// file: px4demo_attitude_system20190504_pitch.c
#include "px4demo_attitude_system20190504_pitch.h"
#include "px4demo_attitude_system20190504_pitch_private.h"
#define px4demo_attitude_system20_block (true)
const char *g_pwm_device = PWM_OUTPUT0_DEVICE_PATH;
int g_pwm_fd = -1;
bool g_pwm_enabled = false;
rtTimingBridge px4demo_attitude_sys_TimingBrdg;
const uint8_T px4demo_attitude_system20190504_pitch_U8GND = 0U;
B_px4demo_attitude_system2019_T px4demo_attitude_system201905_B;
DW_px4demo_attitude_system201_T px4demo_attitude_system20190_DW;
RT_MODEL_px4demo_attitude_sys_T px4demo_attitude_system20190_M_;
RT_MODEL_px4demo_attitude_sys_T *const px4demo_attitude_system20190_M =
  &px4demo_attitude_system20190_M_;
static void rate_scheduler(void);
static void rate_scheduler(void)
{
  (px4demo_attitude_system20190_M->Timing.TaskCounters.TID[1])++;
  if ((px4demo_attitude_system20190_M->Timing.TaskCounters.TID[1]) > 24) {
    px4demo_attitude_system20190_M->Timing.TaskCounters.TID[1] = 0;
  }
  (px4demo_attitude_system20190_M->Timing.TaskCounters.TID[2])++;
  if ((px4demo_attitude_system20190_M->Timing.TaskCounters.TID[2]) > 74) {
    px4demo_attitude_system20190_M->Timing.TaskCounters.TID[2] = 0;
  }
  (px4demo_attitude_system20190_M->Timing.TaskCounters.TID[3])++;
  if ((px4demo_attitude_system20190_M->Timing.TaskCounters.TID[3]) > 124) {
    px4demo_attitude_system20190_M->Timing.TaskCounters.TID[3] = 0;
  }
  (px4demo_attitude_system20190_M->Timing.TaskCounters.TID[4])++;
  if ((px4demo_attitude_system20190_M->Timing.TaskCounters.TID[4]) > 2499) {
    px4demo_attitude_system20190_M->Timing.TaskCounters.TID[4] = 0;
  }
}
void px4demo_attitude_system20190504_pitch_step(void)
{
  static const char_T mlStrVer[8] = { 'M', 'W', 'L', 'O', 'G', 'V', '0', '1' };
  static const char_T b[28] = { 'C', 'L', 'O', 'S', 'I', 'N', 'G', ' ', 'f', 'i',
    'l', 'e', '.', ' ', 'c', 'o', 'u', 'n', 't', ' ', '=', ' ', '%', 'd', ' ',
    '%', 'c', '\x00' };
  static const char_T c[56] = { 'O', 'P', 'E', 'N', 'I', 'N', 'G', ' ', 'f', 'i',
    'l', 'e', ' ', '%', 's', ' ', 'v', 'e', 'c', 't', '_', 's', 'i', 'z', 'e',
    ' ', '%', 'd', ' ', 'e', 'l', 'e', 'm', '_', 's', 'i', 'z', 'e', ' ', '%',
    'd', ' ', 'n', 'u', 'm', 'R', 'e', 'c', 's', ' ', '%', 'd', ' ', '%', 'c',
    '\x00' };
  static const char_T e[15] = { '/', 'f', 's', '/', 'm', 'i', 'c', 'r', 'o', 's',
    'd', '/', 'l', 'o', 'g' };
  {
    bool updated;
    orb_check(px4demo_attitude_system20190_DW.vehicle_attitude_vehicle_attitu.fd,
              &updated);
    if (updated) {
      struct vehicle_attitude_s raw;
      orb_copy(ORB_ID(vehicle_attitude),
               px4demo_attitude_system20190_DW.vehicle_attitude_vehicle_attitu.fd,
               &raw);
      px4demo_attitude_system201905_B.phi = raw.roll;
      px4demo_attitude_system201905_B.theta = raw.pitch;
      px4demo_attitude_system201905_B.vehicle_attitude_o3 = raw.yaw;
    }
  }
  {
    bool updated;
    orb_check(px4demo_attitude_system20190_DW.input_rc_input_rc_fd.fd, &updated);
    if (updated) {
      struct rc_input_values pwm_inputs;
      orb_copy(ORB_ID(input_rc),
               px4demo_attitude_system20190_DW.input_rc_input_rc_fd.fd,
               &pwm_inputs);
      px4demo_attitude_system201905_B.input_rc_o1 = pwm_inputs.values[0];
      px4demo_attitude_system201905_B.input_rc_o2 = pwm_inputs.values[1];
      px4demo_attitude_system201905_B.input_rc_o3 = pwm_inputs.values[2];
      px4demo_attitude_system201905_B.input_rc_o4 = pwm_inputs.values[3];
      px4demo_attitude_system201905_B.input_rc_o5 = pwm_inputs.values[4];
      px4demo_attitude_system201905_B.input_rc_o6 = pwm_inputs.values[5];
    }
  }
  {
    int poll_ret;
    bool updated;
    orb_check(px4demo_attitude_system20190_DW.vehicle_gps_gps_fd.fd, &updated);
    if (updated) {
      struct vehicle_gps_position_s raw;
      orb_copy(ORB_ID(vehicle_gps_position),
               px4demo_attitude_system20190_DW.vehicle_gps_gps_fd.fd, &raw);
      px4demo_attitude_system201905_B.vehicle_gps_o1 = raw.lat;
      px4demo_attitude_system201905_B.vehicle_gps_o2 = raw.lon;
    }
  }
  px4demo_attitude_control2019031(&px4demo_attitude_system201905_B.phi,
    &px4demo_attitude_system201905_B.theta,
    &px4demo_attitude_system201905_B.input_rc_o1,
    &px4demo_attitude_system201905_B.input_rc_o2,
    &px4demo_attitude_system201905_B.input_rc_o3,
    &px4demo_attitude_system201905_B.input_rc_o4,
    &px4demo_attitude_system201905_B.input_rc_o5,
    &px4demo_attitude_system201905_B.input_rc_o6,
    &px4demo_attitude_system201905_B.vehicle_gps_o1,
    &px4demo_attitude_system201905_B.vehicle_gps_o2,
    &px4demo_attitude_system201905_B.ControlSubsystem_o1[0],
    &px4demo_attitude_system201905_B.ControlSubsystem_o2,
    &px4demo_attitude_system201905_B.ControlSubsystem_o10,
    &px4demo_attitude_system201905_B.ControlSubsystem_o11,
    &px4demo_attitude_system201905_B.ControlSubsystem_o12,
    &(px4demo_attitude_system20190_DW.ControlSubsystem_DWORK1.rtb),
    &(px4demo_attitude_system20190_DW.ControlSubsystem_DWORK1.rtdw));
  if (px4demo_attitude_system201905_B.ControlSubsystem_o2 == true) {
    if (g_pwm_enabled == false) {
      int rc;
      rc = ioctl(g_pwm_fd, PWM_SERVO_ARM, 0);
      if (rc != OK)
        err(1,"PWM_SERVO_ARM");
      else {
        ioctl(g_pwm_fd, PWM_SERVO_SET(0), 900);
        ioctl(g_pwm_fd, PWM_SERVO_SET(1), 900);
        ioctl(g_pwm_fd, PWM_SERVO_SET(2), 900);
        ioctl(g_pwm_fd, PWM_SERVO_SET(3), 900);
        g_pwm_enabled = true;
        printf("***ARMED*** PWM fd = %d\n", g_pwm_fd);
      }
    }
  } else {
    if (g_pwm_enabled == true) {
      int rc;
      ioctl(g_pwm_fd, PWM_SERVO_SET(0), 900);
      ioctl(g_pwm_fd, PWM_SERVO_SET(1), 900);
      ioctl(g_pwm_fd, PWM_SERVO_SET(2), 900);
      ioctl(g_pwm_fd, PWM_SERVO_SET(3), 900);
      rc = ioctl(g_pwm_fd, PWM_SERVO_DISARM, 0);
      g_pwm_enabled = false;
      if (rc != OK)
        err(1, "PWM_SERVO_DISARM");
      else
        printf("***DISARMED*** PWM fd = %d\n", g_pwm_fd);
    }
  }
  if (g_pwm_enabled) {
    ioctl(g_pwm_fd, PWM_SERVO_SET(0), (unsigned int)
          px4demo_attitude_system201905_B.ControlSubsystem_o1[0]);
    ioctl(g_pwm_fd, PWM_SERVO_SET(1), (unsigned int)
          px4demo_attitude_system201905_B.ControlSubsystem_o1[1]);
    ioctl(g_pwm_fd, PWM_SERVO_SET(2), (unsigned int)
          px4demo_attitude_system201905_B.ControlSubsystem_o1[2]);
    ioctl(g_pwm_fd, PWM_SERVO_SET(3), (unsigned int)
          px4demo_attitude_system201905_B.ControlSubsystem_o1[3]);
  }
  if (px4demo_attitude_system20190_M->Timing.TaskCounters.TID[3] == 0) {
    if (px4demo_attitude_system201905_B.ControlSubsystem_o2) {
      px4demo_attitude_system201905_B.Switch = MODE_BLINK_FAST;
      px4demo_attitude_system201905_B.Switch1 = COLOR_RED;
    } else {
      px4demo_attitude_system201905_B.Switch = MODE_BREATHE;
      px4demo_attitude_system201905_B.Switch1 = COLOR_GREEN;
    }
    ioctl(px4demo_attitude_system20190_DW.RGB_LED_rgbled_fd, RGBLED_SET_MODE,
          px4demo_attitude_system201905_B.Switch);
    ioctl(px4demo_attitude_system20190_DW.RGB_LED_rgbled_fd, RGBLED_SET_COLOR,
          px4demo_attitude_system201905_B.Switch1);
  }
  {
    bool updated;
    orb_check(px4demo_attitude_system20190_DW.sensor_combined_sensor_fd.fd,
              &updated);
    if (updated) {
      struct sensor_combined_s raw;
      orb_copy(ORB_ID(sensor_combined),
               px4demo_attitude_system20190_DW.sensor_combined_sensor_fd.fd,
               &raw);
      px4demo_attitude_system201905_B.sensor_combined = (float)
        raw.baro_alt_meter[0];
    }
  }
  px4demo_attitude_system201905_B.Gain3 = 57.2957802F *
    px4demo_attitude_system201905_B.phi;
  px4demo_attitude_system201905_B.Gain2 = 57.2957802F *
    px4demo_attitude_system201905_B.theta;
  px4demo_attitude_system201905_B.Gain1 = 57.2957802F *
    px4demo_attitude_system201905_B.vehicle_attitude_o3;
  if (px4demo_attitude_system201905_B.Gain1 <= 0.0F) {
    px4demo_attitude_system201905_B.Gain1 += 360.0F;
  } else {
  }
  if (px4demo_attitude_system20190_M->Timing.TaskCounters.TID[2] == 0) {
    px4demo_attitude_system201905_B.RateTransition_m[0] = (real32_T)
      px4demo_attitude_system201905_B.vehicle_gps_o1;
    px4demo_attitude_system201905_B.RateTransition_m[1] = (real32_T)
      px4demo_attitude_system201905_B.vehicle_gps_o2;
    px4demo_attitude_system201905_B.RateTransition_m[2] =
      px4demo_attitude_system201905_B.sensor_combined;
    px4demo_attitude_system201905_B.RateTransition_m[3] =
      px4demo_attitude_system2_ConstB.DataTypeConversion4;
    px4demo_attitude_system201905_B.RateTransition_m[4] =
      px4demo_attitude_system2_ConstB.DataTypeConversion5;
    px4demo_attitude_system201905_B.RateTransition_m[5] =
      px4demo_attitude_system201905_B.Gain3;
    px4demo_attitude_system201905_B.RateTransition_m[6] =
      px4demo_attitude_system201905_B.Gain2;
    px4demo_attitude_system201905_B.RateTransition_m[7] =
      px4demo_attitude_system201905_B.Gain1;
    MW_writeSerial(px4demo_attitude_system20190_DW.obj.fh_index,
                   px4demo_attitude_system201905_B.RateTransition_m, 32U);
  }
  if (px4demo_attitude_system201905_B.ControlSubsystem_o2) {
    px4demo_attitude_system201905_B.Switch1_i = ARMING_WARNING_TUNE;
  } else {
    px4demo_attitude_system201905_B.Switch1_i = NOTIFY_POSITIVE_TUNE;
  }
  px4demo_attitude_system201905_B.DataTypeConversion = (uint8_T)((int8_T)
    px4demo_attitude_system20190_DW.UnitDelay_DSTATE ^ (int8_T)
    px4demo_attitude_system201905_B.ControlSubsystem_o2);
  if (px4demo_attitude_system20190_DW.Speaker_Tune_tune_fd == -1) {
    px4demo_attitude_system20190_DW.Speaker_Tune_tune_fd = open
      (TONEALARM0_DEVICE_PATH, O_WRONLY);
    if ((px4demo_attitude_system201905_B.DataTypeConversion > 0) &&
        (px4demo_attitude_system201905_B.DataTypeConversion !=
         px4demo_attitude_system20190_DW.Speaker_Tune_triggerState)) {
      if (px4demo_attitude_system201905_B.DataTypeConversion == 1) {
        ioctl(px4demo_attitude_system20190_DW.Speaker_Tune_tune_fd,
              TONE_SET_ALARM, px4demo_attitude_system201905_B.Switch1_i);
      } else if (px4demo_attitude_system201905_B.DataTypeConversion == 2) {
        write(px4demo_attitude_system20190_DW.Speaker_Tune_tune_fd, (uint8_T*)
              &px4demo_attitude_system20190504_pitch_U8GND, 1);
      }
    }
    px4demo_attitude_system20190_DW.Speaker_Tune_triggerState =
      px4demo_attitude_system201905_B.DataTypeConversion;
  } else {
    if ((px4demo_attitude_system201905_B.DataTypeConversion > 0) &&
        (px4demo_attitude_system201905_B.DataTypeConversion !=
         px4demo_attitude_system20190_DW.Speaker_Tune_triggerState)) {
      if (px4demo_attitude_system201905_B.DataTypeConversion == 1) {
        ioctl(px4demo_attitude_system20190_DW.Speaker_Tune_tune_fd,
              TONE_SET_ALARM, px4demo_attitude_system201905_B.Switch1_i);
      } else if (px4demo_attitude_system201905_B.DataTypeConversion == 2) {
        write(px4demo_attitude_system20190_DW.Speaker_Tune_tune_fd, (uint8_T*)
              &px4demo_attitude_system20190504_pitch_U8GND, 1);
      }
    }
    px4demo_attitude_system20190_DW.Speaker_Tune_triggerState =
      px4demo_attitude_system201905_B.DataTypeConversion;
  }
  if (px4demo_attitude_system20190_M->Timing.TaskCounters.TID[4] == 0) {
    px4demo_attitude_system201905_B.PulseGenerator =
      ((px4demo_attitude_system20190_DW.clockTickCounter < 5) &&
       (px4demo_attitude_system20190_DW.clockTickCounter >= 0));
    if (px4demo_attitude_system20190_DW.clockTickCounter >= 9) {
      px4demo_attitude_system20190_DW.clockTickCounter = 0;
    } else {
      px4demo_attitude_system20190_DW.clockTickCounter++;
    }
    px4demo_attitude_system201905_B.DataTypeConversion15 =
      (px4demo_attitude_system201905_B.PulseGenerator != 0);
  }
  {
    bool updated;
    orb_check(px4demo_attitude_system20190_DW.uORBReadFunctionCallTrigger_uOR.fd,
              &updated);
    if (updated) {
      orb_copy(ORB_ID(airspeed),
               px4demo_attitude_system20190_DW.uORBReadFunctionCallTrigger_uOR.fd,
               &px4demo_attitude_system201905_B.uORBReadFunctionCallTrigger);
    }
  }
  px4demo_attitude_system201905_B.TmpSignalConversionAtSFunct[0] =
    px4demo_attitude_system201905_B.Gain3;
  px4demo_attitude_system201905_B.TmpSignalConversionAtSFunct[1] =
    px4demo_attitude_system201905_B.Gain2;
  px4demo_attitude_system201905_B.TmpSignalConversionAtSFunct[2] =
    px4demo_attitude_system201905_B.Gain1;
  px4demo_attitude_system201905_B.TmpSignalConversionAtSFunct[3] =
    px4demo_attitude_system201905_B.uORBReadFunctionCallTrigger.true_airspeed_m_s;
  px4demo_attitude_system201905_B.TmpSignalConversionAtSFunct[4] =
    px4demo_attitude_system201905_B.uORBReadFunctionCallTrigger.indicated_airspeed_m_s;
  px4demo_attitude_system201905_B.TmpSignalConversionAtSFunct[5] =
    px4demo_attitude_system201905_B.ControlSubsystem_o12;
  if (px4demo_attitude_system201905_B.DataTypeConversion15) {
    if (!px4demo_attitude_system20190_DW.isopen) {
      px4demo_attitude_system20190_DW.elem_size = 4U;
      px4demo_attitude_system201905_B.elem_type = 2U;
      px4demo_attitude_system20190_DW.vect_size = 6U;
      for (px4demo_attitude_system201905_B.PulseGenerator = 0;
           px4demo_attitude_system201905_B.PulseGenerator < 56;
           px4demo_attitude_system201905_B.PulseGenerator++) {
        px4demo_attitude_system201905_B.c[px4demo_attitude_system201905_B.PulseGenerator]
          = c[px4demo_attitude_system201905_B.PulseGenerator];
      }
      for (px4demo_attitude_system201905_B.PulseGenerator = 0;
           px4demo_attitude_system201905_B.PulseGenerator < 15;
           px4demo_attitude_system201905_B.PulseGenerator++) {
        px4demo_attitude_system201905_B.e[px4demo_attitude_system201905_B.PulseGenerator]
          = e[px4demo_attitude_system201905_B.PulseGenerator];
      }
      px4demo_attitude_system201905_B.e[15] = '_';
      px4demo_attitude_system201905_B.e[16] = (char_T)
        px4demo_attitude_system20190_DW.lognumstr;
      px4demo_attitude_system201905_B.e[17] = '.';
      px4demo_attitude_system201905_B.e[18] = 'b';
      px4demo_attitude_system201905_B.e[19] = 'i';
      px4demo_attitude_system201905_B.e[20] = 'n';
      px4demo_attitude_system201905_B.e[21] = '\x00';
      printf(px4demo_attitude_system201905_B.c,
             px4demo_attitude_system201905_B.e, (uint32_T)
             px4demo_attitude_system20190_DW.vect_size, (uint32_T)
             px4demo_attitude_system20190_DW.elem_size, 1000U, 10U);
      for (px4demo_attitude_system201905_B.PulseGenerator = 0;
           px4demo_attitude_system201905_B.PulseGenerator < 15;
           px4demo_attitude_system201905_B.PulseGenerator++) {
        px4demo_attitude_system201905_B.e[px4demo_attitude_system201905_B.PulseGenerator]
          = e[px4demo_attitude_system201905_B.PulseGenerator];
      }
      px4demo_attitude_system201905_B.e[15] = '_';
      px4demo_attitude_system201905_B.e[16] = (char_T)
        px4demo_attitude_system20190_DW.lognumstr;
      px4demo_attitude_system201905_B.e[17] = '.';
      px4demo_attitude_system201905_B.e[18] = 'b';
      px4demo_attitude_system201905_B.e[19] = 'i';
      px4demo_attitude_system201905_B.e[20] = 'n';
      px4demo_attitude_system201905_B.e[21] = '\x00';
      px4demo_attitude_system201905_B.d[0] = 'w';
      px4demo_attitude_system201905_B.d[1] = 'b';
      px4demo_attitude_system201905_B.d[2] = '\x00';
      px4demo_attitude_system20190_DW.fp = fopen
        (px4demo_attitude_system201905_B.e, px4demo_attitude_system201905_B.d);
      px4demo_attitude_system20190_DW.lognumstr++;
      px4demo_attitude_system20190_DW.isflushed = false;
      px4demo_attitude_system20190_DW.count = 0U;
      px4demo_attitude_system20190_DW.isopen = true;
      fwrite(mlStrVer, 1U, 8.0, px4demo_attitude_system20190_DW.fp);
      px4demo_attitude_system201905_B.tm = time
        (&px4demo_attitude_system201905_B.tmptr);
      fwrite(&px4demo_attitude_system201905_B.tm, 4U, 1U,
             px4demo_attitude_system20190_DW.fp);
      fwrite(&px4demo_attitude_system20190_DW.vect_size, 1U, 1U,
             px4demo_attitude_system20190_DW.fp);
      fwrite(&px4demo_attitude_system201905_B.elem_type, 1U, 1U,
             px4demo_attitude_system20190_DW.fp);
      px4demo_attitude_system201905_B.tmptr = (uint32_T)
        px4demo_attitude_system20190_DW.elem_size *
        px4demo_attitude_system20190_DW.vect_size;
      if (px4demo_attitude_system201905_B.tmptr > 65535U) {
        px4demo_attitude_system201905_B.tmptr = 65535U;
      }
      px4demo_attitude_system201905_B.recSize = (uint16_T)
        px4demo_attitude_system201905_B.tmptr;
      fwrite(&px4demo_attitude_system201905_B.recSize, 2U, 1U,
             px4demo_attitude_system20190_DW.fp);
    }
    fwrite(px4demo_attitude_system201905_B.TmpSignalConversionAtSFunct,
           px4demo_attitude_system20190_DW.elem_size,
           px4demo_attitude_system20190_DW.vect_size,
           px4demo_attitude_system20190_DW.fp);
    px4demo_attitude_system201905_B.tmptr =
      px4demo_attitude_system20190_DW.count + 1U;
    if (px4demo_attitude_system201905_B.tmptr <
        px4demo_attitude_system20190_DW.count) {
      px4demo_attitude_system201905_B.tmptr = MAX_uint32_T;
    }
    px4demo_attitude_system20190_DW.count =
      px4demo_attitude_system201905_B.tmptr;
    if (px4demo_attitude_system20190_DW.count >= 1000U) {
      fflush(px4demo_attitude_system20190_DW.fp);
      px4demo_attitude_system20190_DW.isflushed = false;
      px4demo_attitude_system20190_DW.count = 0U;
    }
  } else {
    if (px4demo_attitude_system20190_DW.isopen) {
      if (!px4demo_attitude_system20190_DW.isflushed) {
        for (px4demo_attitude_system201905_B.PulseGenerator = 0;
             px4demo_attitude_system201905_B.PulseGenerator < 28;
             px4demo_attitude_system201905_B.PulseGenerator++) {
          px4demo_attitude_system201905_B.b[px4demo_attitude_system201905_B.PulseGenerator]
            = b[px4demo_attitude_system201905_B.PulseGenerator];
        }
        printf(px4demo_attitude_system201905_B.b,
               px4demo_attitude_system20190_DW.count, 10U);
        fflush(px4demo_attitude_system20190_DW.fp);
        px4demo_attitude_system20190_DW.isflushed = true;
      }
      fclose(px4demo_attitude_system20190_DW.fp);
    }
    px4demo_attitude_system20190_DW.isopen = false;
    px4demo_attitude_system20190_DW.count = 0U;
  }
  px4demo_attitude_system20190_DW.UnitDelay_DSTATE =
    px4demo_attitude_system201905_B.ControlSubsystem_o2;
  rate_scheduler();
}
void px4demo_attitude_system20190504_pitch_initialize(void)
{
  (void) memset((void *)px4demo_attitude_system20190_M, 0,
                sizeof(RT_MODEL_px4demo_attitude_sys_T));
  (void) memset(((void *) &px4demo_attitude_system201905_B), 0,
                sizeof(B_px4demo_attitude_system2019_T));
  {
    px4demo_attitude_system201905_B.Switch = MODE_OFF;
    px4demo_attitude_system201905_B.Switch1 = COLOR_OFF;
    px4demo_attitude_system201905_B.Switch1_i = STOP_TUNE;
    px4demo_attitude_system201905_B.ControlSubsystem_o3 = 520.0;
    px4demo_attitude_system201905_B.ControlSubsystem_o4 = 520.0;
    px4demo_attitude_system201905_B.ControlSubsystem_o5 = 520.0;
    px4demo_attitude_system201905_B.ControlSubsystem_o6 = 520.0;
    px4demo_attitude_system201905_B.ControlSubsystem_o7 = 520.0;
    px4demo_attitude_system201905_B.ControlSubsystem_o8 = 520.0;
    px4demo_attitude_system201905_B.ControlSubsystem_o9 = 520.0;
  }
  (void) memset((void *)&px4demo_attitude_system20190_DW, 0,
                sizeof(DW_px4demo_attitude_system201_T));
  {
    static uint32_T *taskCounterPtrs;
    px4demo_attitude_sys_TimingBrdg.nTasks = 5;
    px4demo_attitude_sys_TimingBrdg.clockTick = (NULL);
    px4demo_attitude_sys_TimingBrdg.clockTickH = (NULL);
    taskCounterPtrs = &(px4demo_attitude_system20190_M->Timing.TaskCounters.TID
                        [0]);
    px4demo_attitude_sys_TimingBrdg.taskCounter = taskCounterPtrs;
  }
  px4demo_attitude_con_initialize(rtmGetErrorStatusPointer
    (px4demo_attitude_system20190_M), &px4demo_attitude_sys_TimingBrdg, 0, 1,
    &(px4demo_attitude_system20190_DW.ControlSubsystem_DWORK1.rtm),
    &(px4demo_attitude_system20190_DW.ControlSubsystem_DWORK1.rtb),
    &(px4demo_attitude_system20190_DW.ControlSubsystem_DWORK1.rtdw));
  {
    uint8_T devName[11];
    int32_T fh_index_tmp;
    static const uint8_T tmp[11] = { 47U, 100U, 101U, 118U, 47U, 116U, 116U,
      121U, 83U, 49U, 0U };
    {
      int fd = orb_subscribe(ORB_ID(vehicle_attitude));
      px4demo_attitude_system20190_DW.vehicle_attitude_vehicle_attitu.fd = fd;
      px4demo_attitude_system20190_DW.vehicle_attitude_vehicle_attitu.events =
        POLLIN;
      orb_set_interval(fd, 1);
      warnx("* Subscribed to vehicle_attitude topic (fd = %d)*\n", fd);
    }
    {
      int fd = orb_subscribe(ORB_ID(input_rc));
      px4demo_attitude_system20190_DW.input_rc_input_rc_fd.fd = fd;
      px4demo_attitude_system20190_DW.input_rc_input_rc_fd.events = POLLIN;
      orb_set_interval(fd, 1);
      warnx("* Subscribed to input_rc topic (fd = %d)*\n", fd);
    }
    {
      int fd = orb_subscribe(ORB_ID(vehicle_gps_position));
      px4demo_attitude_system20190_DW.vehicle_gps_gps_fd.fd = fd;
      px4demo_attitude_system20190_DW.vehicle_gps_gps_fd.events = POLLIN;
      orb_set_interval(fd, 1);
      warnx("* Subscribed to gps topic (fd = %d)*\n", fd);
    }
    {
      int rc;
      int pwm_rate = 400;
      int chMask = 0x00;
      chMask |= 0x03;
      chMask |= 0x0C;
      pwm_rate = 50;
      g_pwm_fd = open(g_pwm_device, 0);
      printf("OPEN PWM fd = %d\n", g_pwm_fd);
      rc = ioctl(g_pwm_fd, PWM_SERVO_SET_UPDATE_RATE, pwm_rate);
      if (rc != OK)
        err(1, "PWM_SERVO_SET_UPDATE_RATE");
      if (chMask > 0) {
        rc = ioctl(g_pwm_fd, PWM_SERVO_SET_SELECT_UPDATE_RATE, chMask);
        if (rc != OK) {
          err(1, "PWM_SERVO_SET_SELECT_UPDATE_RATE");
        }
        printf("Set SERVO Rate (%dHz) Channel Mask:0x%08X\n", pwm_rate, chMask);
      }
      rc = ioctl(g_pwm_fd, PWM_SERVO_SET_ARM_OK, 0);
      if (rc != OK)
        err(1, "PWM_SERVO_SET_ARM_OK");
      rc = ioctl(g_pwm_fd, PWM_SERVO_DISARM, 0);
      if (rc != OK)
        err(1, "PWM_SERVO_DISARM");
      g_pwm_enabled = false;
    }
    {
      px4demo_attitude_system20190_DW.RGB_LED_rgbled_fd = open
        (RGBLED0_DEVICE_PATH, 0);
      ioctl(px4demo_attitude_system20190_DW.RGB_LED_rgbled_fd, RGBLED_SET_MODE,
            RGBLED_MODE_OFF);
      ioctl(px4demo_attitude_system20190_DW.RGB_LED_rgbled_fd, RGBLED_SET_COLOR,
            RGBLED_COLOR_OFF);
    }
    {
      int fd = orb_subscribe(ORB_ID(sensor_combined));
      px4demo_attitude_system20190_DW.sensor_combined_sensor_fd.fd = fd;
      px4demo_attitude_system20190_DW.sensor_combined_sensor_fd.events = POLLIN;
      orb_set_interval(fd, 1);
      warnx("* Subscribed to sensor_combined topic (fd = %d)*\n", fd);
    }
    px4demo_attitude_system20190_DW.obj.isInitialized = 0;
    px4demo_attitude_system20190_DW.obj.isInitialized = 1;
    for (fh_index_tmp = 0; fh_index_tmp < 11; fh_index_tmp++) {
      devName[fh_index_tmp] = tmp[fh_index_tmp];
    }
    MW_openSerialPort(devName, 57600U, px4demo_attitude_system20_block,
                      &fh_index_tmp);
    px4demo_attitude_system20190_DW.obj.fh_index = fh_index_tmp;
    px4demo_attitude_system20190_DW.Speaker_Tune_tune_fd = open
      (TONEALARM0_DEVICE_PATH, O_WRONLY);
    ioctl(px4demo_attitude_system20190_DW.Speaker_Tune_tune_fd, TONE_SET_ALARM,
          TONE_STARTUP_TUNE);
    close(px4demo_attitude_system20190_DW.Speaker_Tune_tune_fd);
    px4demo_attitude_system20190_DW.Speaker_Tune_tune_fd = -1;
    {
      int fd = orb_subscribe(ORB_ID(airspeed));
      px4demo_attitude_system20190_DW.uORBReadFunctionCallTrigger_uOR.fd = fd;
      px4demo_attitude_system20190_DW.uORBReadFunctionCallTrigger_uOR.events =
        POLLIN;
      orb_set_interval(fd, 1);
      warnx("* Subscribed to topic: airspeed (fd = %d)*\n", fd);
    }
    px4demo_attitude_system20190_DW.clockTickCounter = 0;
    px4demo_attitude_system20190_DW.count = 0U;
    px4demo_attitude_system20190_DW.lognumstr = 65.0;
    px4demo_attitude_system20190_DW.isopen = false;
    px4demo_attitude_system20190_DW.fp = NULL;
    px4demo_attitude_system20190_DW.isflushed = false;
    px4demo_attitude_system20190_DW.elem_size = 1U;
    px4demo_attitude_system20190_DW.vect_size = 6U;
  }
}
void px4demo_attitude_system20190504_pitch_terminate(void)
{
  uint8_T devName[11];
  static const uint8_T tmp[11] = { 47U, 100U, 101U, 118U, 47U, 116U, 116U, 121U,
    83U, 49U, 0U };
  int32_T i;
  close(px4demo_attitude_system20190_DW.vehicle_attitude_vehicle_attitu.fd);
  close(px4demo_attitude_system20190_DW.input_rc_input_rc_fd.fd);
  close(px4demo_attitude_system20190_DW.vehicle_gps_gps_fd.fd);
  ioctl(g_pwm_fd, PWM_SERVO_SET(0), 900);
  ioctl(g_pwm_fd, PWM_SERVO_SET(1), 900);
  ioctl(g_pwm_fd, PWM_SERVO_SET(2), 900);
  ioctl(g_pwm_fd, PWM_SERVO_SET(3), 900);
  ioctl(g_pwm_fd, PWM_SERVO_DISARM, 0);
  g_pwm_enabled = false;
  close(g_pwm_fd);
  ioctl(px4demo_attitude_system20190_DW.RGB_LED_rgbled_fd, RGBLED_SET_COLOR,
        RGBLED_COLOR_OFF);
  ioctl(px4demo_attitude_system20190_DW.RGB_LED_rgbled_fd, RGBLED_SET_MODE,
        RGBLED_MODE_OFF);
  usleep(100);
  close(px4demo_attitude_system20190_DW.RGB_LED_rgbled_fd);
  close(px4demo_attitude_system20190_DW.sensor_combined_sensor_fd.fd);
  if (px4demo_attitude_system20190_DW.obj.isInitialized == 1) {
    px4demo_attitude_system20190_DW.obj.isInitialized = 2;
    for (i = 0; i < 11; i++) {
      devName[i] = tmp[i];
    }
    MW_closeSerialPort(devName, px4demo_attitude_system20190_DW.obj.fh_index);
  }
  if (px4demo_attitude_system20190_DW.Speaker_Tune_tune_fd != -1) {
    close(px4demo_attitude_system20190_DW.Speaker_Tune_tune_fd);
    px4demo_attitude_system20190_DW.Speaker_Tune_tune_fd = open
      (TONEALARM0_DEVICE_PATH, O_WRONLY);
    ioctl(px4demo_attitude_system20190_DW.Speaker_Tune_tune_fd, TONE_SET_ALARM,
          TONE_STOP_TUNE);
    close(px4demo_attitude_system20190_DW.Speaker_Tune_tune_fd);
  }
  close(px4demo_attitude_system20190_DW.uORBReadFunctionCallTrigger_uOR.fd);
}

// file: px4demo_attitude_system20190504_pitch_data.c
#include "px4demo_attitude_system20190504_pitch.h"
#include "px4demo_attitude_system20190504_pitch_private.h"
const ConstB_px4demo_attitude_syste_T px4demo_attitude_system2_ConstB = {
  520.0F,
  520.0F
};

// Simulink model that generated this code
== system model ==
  PWM_output#1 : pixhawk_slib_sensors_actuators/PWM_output  <- 1: ControlSubsystem/2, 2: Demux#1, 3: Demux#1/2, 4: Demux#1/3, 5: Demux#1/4
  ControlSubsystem : ModelReference  <- 1: vehicle_attitude, 2: vehicle_attitude/2, 3: input_rc, 4: input_rc/2, 5: input_rc/3, 6: input_rc/4, 7: input_rc/5, 8: input_rc/6, 9: vehicle_gps, 10: vehicle_gps/2, 11: vehicle_attitude/3
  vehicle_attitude : pixhawk_slib_sensors_actuators/vehicle_attitude
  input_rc : pixhawk_slib_sensors_actuators/input_rc
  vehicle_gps : pixhawk_slib_sensors_actuators/vehicle_gps
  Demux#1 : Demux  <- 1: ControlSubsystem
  RGB_LED : pixhawk_slib_sensors_actuators/RGB_LED  <- 1: Switch, 2: Switch1
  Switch : Switch  Criteria=u2 ~= 0  Threshold=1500  <- 1: Constant#1, 2: ControlSubsystem/2, 3: Constant#2
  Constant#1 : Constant  Value=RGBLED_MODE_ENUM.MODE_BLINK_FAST
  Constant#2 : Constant  Value=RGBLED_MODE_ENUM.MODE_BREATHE
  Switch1 : Switch  Criteria=u2 ~= 0  Threshold=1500  <- 1: Constant#3, 2: ControlSubsystem/2, 3: Constant#4
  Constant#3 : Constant  Value=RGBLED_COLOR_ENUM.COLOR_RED
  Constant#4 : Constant  Value=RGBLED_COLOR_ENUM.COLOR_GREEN
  Serial#1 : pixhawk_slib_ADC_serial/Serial  <- 1: RateTransition
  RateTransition : RateTransition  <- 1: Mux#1
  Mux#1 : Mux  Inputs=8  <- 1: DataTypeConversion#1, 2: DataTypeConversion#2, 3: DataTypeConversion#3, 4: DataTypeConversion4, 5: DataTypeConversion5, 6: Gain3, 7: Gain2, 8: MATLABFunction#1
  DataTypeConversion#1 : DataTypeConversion  <- 1: vehicle_gps
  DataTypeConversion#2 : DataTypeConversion  <- 1: vehicle_gps/2
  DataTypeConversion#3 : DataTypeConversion  <- 1: sensor_combined
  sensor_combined : pixhawk_slib_sensors_actuators/sensor_combined
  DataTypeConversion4 : DataTypeConversion  <- 1: ControlSubsystem/8
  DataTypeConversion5 : DataTypeConversion  <- 1: ControlSubsystem/9
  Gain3 : Gain  Gain=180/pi  <- 1: DataTypeConversion#4
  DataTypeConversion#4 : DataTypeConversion  <- 1: vehicle_attitude
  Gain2 : Gain  Gain=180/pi  <- 1: DataTypeConversion#5
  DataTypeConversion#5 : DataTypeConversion  <- 1: vehicle_attitude/2
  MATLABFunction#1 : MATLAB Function  <- 1: Gain1
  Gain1 : Gain  Gain=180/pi  <- 1: DataTypeConversion#6
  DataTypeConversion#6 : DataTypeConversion  <- 1: vehicle_attitude/3
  Speaker_Tune : pixhawk_slib_sensors_actuators/Speaker_Tune  <- 1: Switch#1, 3: DataTypeConversion
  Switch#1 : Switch  Criteria=u2 ~= 0  Threshold=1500  <- 1: Constant#5, 2: ControlSubsystem/2, 3: Constant#6
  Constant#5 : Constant  Value=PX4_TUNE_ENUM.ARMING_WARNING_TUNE
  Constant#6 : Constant  Value=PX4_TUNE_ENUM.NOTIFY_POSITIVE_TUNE
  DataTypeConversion : DataTypeConversion  <- 1: Logic#1
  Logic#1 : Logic  Operator=XOR  <- 1: UnitDelay, 2: ControlSubsystem/2
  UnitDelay : UnitDelay  <- 1: ControlSubsystem/2
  binary_logger#1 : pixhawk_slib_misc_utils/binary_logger  <- 1: DataTypeConversion15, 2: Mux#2
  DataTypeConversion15 : DataTypeConversion  <- 1: PulseGenerator
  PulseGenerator : DiscretePulseGenerator  Period=10  PulseWidth=5
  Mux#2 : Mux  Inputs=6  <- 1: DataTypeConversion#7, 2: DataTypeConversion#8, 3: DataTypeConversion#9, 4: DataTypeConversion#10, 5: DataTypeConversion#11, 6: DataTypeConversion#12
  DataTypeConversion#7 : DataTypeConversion  <- 1: Gain3
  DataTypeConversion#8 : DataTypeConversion  <- 1: Gain2
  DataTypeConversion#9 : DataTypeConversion  <- 1: MATLABFunction#1
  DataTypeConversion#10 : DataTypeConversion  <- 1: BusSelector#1
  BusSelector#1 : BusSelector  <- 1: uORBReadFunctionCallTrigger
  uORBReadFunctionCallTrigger : pixhawk_slib_uORB_RW/uORB Read // Function-Call Trigger
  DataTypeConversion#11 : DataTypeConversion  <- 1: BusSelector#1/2
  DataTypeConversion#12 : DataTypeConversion  <- 1: ControlSubsystem/12
== matlab function MATLABFunction#1 ==
function y = fcn(u)
if(u<=0)
    y=360+u;
else
    y=u
end
